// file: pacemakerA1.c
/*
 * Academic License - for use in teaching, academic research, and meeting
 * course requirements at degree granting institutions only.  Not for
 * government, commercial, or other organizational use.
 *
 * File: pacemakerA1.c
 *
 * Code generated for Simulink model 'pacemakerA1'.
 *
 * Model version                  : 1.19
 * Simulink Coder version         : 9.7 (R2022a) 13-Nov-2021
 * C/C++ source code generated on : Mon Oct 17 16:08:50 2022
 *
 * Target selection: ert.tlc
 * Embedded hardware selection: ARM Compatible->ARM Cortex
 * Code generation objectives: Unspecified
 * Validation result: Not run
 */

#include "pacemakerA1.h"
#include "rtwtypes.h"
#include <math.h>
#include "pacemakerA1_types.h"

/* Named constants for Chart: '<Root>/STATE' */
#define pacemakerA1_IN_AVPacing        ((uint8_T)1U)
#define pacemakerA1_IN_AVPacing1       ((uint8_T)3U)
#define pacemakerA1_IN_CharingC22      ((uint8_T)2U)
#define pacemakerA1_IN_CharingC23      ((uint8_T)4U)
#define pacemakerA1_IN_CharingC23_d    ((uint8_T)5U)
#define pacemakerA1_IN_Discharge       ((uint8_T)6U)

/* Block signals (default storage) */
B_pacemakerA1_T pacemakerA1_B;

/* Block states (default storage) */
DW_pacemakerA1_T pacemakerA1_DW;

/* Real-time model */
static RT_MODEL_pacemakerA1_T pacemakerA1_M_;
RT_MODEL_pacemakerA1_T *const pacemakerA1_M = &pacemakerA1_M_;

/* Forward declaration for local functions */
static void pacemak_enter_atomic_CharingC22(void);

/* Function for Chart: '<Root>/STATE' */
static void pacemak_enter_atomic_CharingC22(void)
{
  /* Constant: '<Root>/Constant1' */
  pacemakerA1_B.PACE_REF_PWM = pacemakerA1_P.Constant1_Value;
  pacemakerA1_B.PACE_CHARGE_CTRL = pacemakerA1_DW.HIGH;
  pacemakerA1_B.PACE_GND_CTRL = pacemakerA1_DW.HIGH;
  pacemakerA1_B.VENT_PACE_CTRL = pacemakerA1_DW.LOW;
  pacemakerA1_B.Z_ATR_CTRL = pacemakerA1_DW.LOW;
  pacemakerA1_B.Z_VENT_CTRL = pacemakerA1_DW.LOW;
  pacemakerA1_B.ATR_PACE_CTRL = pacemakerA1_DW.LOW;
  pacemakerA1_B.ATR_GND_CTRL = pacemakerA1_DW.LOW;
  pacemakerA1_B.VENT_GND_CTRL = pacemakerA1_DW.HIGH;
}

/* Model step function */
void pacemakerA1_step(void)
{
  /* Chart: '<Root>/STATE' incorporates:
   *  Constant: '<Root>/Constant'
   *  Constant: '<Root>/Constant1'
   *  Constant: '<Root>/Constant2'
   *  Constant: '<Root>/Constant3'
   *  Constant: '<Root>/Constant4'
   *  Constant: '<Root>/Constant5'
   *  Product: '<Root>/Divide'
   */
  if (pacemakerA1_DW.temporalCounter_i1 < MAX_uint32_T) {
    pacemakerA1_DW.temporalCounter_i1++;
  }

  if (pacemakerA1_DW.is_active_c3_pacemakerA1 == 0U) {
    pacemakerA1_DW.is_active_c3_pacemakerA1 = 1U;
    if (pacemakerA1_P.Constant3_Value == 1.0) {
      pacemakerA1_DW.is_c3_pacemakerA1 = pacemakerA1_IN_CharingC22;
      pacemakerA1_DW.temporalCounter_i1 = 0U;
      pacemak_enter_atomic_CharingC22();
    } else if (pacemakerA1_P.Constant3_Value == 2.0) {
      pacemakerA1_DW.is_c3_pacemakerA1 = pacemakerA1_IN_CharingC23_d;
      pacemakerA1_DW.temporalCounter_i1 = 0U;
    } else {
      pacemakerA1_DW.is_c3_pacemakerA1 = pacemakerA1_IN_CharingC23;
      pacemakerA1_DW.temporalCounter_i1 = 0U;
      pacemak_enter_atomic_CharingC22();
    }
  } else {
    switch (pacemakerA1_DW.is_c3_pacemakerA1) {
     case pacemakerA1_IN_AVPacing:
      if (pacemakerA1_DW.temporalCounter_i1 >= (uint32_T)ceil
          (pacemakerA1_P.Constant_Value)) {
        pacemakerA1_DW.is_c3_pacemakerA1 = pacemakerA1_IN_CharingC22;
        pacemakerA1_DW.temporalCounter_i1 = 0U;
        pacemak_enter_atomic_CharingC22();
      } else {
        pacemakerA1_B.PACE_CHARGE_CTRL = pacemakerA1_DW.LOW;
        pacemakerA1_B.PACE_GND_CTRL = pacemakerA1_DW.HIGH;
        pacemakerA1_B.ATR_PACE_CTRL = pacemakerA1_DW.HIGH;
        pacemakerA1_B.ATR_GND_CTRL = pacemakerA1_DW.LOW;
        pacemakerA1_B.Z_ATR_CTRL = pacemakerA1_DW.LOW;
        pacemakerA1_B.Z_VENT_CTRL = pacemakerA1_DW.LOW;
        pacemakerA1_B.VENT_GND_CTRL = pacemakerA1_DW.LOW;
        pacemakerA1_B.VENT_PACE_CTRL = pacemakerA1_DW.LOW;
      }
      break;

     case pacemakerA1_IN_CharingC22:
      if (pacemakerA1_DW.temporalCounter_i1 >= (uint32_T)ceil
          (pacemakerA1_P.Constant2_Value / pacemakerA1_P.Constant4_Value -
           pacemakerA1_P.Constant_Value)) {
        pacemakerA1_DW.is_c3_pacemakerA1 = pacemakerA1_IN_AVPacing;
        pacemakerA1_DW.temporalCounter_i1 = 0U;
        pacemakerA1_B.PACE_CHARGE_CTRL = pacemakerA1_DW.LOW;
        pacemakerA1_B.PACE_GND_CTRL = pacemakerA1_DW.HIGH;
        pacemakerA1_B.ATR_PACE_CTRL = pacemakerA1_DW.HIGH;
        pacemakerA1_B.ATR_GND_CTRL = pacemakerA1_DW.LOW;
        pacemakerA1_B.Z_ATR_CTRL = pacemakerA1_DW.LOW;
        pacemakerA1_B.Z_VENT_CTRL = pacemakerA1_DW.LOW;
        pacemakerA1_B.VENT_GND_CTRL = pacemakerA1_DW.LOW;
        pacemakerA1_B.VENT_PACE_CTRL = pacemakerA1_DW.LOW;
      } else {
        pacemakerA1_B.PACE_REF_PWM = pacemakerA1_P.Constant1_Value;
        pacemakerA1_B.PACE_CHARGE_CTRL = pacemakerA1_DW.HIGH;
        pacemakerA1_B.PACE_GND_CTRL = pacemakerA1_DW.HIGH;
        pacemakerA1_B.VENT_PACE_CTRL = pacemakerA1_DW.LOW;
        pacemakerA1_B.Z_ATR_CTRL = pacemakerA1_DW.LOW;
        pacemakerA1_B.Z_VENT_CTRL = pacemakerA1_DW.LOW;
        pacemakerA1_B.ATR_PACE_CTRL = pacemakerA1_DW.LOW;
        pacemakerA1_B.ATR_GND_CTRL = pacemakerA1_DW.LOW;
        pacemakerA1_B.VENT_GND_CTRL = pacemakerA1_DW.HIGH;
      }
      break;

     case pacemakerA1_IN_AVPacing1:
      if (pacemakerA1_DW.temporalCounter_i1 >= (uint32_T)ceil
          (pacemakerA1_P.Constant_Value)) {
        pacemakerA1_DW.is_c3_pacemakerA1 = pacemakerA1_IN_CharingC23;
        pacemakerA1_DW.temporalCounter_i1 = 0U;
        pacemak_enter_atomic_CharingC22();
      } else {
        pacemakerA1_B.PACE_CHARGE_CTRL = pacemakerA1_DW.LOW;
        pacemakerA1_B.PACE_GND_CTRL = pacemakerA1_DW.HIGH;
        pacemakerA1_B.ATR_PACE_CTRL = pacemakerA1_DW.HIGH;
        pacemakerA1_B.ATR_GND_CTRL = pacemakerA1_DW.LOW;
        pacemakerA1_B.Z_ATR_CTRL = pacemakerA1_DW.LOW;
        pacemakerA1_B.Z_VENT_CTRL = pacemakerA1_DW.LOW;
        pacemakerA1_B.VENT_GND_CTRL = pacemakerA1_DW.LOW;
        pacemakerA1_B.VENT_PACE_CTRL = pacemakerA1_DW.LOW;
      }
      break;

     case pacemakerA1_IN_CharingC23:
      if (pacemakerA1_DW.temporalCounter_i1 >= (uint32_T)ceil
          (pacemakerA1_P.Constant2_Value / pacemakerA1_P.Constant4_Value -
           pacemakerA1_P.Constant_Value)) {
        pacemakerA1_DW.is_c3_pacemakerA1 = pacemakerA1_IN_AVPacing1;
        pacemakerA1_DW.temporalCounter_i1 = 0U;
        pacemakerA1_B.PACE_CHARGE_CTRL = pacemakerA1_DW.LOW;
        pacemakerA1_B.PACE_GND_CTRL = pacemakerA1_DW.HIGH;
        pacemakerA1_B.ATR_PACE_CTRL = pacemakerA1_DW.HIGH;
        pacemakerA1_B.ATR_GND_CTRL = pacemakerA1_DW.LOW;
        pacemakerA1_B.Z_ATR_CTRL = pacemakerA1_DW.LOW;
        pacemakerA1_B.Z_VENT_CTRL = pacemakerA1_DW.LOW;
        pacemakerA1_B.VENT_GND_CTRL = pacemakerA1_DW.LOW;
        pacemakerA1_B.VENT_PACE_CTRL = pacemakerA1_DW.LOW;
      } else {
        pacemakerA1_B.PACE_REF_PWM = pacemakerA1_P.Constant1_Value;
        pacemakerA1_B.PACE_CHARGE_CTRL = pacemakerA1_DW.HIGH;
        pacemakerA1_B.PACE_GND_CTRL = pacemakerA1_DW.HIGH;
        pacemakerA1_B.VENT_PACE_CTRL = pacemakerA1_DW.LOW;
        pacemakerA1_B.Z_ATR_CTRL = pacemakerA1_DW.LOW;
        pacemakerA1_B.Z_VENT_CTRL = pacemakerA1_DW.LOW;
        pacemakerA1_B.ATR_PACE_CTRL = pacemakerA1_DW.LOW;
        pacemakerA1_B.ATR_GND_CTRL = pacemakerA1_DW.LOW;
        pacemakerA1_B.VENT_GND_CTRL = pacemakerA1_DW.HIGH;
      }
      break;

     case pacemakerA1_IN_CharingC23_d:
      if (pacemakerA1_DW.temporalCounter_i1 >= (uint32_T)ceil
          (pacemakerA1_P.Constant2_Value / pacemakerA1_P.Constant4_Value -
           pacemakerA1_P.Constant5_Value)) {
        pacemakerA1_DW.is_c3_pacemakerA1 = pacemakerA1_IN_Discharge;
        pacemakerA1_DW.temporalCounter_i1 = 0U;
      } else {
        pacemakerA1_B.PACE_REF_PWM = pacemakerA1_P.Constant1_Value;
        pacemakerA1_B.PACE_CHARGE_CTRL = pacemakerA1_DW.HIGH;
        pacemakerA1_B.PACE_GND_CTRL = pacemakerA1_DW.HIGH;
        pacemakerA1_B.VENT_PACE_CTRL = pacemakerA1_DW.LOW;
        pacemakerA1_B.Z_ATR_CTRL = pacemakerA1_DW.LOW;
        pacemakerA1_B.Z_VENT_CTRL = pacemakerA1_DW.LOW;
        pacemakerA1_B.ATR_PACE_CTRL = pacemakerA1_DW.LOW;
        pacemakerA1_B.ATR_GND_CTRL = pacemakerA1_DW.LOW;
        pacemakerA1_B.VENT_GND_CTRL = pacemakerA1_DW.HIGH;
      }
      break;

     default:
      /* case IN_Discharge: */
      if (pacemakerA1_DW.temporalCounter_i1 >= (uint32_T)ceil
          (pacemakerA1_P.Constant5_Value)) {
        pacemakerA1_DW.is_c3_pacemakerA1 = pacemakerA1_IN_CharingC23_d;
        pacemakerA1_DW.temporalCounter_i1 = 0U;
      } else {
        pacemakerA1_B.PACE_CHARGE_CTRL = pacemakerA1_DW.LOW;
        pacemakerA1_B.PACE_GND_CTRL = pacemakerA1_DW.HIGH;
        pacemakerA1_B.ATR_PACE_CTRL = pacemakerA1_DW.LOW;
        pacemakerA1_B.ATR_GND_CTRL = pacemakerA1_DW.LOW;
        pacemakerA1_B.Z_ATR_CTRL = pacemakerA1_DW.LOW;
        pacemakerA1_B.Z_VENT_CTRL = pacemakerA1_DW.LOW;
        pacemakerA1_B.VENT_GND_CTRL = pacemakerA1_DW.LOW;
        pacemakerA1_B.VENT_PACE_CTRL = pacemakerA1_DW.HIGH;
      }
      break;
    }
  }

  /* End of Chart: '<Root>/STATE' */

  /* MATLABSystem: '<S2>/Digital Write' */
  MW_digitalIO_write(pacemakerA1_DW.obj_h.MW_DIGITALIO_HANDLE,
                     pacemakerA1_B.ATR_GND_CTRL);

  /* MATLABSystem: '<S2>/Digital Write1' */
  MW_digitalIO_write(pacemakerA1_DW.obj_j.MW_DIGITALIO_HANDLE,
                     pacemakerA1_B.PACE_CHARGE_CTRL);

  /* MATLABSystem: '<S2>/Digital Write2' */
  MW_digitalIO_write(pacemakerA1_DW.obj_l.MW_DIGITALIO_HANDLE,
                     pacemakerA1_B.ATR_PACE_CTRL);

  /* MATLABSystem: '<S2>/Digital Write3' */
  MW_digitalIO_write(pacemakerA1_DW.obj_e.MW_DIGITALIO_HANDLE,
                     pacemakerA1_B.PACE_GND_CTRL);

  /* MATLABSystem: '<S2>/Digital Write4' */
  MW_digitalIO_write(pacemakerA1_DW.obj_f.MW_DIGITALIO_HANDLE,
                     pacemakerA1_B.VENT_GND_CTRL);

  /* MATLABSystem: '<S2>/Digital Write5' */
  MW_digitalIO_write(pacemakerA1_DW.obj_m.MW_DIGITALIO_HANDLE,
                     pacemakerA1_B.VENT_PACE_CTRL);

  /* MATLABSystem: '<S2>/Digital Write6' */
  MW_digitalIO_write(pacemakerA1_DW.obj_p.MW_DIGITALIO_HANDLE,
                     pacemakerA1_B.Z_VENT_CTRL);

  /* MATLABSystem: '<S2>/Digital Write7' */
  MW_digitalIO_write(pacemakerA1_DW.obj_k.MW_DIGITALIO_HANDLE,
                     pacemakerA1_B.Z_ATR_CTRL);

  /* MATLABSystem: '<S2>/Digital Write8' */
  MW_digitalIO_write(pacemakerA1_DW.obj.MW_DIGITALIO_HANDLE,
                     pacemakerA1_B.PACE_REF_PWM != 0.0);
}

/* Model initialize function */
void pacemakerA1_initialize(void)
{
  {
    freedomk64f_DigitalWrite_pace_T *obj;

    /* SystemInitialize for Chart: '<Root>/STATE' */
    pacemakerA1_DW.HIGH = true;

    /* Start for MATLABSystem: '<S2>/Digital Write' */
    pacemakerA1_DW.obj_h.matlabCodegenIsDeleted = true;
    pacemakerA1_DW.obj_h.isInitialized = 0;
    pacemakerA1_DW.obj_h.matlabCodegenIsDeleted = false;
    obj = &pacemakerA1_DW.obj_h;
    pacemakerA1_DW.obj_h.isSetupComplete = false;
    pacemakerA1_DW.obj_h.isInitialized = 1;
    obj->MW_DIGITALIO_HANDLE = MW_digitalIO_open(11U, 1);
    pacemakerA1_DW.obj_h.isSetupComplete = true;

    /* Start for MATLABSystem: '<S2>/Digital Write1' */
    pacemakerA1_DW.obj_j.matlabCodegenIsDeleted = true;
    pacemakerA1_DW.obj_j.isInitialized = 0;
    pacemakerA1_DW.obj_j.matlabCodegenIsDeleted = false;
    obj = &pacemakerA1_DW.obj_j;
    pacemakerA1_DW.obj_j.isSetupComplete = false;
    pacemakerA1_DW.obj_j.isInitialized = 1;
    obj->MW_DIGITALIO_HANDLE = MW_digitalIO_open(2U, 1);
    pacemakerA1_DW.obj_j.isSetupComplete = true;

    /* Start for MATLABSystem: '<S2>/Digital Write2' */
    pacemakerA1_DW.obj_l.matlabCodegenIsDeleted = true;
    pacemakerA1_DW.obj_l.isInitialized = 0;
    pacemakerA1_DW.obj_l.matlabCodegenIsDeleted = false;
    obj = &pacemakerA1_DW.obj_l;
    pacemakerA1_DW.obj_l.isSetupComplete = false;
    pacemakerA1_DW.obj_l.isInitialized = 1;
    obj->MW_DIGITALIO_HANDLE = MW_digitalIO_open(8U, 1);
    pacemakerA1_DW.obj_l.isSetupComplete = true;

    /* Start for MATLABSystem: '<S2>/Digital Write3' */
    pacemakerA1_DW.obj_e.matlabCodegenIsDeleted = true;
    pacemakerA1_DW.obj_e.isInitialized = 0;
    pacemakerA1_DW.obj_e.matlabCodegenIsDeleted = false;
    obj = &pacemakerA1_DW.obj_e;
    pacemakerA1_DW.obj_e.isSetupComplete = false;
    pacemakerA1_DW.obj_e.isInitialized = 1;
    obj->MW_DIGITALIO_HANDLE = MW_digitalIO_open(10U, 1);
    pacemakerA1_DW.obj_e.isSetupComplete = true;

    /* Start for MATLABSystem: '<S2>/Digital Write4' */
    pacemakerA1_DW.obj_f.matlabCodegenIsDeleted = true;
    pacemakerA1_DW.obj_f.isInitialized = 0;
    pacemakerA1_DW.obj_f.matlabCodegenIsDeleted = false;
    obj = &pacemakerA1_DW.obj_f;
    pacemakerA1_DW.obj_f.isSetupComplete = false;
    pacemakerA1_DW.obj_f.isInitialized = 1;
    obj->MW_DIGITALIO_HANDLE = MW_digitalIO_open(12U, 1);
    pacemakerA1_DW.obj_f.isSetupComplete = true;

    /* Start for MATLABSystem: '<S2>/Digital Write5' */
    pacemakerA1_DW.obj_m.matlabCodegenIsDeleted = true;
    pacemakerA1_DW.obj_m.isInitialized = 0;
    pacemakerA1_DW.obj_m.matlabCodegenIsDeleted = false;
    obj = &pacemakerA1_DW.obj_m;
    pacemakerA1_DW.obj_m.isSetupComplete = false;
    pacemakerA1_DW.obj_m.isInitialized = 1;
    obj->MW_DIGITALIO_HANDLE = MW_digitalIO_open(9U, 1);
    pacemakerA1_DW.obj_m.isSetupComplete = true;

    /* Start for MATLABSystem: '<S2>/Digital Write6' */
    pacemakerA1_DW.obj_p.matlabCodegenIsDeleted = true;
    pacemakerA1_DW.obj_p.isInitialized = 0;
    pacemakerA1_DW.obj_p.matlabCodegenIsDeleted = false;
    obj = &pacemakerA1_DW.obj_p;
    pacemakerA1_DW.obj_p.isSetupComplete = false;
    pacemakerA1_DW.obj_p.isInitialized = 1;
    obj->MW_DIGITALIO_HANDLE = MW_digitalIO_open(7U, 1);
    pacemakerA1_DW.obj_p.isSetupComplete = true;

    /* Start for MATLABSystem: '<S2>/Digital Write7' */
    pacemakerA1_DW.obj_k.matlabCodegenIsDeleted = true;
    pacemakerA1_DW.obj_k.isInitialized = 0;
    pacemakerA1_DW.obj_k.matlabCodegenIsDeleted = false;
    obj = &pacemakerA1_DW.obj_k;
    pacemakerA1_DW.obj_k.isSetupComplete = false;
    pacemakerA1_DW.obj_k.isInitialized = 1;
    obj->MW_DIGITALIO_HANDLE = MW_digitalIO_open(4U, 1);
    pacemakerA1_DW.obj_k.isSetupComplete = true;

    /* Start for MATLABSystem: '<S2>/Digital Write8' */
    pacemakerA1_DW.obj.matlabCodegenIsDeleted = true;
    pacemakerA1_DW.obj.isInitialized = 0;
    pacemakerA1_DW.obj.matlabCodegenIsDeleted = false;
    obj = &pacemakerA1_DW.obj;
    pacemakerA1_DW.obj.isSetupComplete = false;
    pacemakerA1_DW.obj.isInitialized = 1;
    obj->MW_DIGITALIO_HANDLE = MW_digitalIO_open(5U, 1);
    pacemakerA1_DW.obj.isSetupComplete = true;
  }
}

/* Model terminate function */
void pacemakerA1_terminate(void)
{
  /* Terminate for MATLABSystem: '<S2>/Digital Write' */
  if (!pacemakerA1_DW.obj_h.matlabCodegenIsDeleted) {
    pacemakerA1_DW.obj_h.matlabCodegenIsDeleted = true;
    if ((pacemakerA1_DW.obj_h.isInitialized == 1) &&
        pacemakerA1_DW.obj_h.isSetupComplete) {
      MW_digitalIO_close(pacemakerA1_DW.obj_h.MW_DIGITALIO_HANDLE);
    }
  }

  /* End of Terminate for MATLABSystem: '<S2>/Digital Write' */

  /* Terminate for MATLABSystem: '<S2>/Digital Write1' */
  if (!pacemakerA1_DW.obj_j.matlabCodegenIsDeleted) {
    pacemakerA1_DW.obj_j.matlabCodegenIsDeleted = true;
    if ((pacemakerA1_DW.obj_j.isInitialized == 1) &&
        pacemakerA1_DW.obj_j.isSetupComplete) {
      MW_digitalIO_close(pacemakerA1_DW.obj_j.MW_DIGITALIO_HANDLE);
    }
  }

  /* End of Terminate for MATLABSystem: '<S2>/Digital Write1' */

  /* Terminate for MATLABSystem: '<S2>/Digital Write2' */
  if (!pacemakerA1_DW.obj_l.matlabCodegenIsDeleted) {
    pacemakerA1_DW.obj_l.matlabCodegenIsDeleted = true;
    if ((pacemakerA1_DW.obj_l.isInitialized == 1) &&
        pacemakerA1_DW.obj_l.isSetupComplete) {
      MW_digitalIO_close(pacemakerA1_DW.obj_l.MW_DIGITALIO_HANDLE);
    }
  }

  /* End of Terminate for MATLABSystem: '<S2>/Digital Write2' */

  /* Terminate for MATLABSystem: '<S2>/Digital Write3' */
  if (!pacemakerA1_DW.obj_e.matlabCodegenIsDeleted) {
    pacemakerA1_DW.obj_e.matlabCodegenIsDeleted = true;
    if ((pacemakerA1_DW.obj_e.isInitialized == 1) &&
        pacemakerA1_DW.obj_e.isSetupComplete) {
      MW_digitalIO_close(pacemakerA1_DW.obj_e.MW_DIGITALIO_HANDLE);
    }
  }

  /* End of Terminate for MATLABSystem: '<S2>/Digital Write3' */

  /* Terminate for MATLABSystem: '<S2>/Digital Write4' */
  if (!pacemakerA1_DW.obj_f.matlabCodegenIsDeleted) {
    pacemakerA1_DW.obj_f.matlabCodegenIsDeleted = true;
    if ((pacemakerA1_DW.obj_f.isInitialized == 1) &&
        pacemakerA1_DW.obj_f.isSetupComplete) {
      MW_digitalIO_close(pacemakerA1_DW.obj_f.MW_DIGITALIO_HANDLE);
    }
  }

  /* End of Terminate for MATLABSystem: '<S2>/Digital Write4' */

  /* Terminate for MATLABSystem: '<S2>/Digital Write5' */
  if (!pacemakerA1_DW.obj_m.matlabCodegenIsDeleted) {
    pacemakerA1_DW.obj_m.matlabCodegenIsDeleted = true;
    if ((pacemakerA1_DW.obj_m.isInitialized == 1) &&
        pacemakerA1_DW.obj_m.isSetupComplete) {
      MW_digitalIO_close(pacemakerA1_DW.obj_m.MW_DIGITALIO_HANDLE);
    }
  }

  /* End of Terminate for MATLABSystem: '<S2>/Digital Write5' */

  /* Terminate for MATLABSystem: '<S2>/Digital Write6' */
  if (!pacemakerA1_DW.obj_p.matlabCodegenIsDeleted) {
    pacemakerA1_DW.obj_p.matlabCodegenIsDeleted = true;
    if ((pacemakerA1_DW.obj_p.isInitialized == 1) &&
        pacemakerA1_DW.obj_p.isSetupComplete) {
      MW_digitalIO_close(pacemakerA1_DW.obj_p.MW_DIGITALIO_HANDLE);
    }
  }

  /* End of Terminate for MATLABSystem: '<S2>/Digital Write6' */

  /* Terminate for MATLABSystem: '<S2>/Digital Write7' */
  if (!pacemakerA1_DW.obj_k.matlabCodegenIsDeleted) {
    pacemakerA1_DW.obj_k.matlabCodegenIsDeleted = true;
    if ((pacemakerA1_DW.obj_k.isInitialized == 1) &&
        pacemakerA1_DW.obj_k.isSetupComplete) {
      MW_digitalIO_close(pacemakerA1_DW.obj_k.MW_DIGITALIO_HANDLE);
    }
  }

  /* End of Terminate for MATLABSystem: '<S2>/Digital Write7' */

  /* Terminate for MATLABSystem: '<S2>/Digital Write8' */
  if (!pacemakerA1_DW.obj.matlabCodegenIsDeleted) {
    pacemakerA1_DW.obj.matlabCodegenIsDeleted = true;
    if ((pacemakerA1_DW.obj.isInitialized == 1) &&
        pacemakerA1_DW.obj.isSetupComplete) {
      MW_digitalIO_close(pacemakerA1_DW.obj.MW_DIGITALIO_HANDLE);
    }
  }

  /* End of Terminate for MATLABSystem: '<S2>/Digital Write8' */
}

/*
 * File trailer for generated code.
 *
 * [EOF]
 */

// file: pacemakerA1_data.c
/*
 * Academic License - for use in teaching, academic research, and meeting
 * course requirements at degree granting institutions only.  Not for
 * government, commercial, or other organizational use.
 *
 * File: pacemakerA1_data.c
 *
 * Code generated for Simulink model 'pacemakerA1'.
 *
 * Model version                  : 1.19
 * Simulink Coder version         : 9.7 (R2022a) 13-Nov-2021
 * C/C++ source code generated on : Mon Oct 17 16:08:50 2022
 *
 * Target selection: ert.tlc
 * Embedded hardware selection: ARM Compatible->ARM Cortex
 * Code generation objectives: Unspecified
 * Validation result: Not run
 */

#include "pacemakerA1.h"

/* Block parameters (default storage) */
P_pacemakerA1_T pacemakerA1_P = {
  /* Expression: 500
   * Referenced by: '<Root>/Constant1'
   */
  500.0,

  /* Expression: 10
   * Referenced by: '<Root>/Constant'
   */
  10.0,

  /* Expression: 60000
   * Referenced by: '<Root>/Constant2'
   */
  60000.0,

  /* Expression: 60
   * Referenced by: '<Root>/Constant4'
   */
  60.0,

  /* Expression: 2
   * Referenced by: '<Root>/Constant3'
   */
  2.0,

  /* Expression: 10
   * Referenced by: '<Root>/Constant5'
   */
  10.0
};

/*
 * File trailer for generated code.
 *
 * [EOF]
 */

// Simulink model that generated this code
simulink model "pacemakerA1"  (R2022a)
settings: Solver=FixedStepAuto  StartTime=0.0  StopTime=10.0  FixedStep=1e-3  RelTol=1e-3  EnableMultiTasking=on
undefined symbols (not defined in the file): D10, D11, D12, D2, D4, D5, D7, D8, D9, PTA0, PTA2, PTB23, PTB9, PTC3, PTC4, PTD0, PTD2, PTD3
libraries: frdmk64flib x9

== system pacemakerA1 ==
  Constant : Constant
  Constant1 : Constant  Value=500
  Constant2 : Constant  Value=60000
  Constant3 : Constant  Value=2
  Constant4 : Constant  Value=60
  Constant5 : Constant  Value=10
  Divide : Product  Inputs=*/
  STATE : Stateflow chart  TreatAsAtomicUnit=on
  Subsystem : Subsystem
  wires:
  STATE/1(ATR_GND_CTRL) -> [ATR_GND_CTRL]
  STATE/2(PACE_CHARGE_CTRL) -> [PACE_CHARGE_CTRL]
  STATE/3(ATR_PACE_CTRL) -> [ATR_PACE_CTRL]
  STATE/4(PACE_GND_CTRL) -> [PACE_GND_CTRL]
  STATE/5(VENT_GND_CTRL) -> [VENT_GND_CTRL]
  STATE/6(VENT_PACE_CTRL) -> [VENT_PACE_CTRL]
  STATE/7(Z_VENT_CTRL) -> [Z_VENT_CTRL]
  STATE/8(Z_ATR_CTRL) -> [Z_ATR_CTRL]
  STATE/9(PACE_REF_PWM) -> [PACE_REF_PWM]
  [ATR_DUTY_CYCLE] -> STATE/1(ATR_DUTY_CYCLE)
  [ATR_PW] -> STATE/2(ATR_PW)
  [PERIOD] -> STATE/3(PERIOD)
  Constant1/1 -> [VENT_DUTY_CYCLE], [ATR_DUTY_CYCLE]
  Constant/1 -> [ATR_PW]
  Divide/1 -> [PERIOD]
  Constant4/1 -> Divide/2
  Constant2/1 -> Divide/1
  [ATR_GND_CTRL] -> Subsystem/1(In1)
  [PACE_CHARGE_CTRL] -> Subsystem/2(In2)
  [ATR_PACE_CTRL] -> Subsystem/3(In3)
  [PACE_GND_CTRL] -> Subsystem/4(In4)
  [VENT_GND_CTRL] -> Subsystem/5(In5)
  [VENT_PACE_CTRL] -> Subsystem/6(In6)
  [Z_VENT_CTRL] -> Subsystem/7(In7)
  [Z_ATR_CTRL] -> Subsystem/8(In8)
  [PACE_REF_PWM] -> Subsystem/9(In9)
  Constant3/1 -> STATE/4(MODE)
  Constant5/1 -> STATE/5(VENT_PW)
  [VENT_DUTY_CYCLE] -> STATE/6(VENT_DUTY_CYCLE)

== system pacemakerA1/Subsystem ==
  In1 : Inport
  In2 : Inport  Port=2
  In3 : Inport  Port=3
  In4 : Inport  Port=4
  In5 : Inport  Port=5
  In6 : Inport  Port=6
  In7 : Inport  Port=7
  In8 : Inport  Port=8
  In9 : Inport  Port=9
  Digital Write : frdmk64flib/Digital Write  Whichpin=PTD2 (D11)
  Digital Write1 : frdmk64flib/Digital Write  Whichpin=PTB9 (D2)
  Digital Write2 : frdmk64flib/Digital Write  Whichpin=PTA0 (D8)
  Digital Write3 : frdmk64flib/Digital Write  Whichpin=PTD0 (D10)
  Digital Write4 : frdmk64flib/Digital Write  Whichpin=PTD3 (D12)
  Digital Write5 : frdmk64flib/Digital Write  Whichpin=PTC4 (D9)
  Digital Write6 : frdmk64flib/Digital Write  Whichpin=PTC3 (D7)
  Digital Write7 : frdmk64flib/Digital Write  Whichpin=PTB23 (D4)
  Digital Write8 : frdmk64flib/Digital Write  Whichpin=PTA2 (D5)
  Scope : Scope  NumInputPorts=9
  wires:
  In7/1 -> Scope/7, Digital Write6/1
  In2/1 -> Scope/2, Digital Write1/1
  In6/1 -> Scope/6, Digital Write5/1
  In4/1 -> Scope/4, Digital Write3/1
  In3/1 -> Scope/3, Digital Write2/1
  In9/1 -> Scope/9, Digital Write8/1
  In1/1 -> Scope/1, Digital Write/1
  In8/1 -> Scope/8, Digital Write7/1
  In5/1 -> Scope/5, Digital Write4/1

== stateflow chart pacemakerA1/STATE ==
  state AOO [group]
    state CharingC22
      %Capacitor charing state
      ATR_PACE_CTRL = LOW
      VENT_PACE_CTRL = LOW
      PACE_REF_PWM = ATR_DUTY_CYCLE
      PACE_CHARGE_CTRL = HIGH
      %Discharge capacitor
      PACE_GND_CTRL = HIGH
      VENT_PACE_CTRL = LOW
      Z_ATR_CTRL = LOW
      Z_VENT_CTRL = LOW
      ATR_PACE_CTRL = LOW
      ATR_GND_CTRL = LOW
      VENT_GND_CTRL = HIGH
    state AVPacing
      %step 2
      PACE_CHARGE_CTRL = LOW
      PACE_GND_CTRL = HIGH
      ATR_PACE_CTRL = HIGH
      ATR_GND_CTRL = LOW
      Z_ATR_CTRL = LOW
      Z_VENT_CTRL = LOW
      VENT_GND_CTRL = LOW
      VENT_PACE_CTRL = LOW
    CharingC22 -> AVPacing : after(PERIOD-ATR_PW, msec)
    AVPacing -> CharingC22 : after(ATR_PW, msec)
  state VOO [group]
    state CharingC23
      during:
      %Begin Charging C22 Capacitor
      ATR_PACE_CTRL = LOW
      VENT_PACE_CTRL = LOW
      PACE_REF_PWM = VENT_DUTY_CYCLE
      PACE_CHARGE_CTRL = HIGH
      %Begin Discharging C21 Blocking Capacitor
      PACE_GND_CTRL = HIGH
      VENT_PACE_CTRL = LOW
      Z_ATR_CTRL = LOW
      Z_VENT_CTRL = LOW
      ATR_PACE_CTRL = LOW
      ATR_GND_CTRL = LOW
      VENT_GND_CTRL = HIGH
    state Discharge
      during:
      %Discharge C22 into Ventricle (Vent Pacing)
      %Begin Charging Blocking Capacitor
      PACE_CHARGE_CTRL = LOW
      PACE_GND_CTRL = HIGH
      ATR_PACE_CTRL = LOW
      ATR_GND_CTRL = LOW
      Z_ATR_CTRL = LOW
      Z_VENT_CTRL = LOW
      VENT_GND_CTRL = LOW
      VENT_PACE_CTRL  = HIGH
    VOO.CharingC23 -> Discharge : after(PERIOD-VENT_PW, msec)
    Discharge -> VOO.CharingC23 : after(VENT_PW, msec)
  state TEST [group]
    state CharingC23
      %Capacitor charing state
      ATR_PACE_CTRL = LOW
      VENT_PACE_CTRL = LOW
      PACE_REF_PWM = ATR_DUTY_CYCLE
      PACE_CHARGE_CTRL = HIGH
      %Discharge capacitor
      PACE_GND_CTRL = HIGH
      VENT_PACE_CTRL = LOW
      Z_ATR_CTRL = LOW
      Z_VENT_CTRL = LOW
      ATR_PACE_CTRL = LOW
      ATR_GND_CTRL = LOW
      VENT_GND_CTRL = HIGH
    state AVPacing1
      %step 2
      PACE_CHARGE_CTRL = LOW
      PACE_GND_CTRL = HIGH
      ATR_PACE_CTRL = HIGH
      ATR_GND_CTRL = LOW
      Z_ATR_CTRL = LOW
      Z_VENT_CTRL = LOW
      VENT_GND_CTRL = LOW
      VENT_PACE_CTRL = LOW
    TEST.CharingC23 -> AVPacing1 : after(PERIOD-ATR_PW, msec)
    AVPacing1 -> TEST.CharingC23 : after(ATR_PW, msec)
  (junction 37) -> CharingC22 [order 1] : [MODE ==1]
  (junction 37) -> VOO.CharingC23 [order 2] : [MODE ==2]
  (default) -> (junction 37)
  (junction 37) -> TEST.CharingC23 [order 3]
  data: HIGH local =true; LOW local =false; ATR_GND_CTRL output; PACE_CHARGE_CTRL output; ATR_PACE_CTRL output; PACE_GND_CTRL output; VENT_GND_CTRL output; VENT_PACE_CTRL output; Z_VENT_CTRL output; Z_ATR_CTRL output; PACE_REF_PWM output; ATR_DUTY_CYCLE input; ATR_PW input; PERIOD input; MODE input; VENT_PW input; VENT_DUTY_CYCLE input
